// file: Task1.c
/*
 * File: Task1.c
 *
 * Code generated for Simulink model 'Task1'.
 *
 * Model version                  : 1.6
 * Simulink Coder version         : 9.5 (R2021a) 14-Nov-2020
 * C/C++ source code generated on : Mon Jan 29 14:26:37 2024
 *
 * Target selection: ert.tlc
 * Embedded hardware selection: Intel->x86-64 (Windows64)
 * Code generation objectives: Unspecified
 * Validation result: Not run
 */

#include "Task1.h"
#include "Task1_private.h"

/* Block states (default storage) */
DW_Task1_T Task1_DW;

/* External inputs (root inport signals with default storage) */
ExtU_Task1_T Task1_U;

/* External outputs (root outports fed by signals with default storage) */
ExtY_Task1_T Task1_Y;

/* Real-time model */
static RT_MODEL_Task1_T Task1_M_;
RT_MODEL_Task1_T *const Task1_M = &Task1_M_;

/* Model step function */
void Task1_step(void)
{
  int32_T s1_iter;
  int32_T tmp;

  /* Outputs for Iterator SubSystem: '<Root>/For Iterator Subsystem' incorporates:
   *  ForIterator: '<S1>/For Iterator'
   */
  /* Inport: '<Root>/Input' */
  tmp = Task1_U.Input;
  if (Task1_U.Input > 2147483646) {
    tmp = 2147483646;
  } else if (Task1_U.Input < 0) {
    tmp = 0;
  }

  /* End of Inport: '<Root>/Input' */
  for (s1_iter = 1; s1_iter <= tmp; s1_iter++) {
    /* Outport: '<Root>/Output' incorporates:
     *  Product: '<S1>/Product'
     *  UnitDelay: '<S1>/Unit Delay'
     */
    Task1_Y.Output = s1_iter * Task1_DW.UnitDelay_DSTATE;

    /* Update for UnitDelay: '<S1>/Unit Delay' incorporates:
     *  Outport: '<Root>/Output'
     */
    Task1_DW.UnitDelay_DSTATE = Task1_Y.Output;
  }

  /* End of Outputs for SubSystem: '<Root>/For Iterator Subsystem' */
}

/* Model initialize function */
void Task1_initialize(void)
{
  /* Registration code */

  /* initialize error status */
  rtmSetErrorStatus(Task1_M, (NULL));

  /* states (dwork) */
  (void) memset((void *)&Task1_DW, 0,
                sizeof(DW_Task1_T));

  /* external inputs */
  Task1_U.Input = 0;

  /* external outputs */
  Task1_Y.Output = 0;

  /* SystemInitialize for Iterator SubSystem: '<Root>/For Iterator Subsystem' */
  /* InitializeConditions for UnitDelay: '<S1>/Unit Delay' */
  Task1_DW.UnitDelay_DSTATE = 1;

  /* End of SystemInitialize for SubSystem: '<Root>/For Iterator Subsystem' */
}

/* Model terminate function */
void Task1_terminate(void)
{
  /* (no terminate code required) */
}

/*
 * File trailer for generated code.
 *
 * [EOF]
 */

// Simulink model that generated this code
simulink model "Task1"  (R2021a)
settings: Solver=FixedStepDiscrete  StartTime=0.0  StopTime=10.0  RelTol=1e-3  EnableMultiTasking=on

== system Task1 ==
  Input : Inport
  For Iterator Subsystem : Subsystem  TreatAsAtomicUnit=on
  Output : Outport
  wires:
  Input/1 -> For Iterator Subsystem/1(Input)
  For Iterator Subsystem/1(Out1) -> Output/1

== system Task1/For Iterator Subsystem ==
  Input : Inport  OutDataTypeStr=int32
  For Iterator : ForIterator  IterationSource=external
  Product : Product  OutDataTypeStr=int32
  Unit Delay : UnitDelay  InitialCondition=1  SampleTime=-1  HasFrameUpgradeWarning=on
  Out1 : Outport  OutDataTypeStr=int32
  wires:
  Input/1 -> For Iterator/1
  For Iterator/1 -> Product/1
  Product/1 -> Unit Delay/1, Out1/1
  Unit Delay/1 -> Product/2
